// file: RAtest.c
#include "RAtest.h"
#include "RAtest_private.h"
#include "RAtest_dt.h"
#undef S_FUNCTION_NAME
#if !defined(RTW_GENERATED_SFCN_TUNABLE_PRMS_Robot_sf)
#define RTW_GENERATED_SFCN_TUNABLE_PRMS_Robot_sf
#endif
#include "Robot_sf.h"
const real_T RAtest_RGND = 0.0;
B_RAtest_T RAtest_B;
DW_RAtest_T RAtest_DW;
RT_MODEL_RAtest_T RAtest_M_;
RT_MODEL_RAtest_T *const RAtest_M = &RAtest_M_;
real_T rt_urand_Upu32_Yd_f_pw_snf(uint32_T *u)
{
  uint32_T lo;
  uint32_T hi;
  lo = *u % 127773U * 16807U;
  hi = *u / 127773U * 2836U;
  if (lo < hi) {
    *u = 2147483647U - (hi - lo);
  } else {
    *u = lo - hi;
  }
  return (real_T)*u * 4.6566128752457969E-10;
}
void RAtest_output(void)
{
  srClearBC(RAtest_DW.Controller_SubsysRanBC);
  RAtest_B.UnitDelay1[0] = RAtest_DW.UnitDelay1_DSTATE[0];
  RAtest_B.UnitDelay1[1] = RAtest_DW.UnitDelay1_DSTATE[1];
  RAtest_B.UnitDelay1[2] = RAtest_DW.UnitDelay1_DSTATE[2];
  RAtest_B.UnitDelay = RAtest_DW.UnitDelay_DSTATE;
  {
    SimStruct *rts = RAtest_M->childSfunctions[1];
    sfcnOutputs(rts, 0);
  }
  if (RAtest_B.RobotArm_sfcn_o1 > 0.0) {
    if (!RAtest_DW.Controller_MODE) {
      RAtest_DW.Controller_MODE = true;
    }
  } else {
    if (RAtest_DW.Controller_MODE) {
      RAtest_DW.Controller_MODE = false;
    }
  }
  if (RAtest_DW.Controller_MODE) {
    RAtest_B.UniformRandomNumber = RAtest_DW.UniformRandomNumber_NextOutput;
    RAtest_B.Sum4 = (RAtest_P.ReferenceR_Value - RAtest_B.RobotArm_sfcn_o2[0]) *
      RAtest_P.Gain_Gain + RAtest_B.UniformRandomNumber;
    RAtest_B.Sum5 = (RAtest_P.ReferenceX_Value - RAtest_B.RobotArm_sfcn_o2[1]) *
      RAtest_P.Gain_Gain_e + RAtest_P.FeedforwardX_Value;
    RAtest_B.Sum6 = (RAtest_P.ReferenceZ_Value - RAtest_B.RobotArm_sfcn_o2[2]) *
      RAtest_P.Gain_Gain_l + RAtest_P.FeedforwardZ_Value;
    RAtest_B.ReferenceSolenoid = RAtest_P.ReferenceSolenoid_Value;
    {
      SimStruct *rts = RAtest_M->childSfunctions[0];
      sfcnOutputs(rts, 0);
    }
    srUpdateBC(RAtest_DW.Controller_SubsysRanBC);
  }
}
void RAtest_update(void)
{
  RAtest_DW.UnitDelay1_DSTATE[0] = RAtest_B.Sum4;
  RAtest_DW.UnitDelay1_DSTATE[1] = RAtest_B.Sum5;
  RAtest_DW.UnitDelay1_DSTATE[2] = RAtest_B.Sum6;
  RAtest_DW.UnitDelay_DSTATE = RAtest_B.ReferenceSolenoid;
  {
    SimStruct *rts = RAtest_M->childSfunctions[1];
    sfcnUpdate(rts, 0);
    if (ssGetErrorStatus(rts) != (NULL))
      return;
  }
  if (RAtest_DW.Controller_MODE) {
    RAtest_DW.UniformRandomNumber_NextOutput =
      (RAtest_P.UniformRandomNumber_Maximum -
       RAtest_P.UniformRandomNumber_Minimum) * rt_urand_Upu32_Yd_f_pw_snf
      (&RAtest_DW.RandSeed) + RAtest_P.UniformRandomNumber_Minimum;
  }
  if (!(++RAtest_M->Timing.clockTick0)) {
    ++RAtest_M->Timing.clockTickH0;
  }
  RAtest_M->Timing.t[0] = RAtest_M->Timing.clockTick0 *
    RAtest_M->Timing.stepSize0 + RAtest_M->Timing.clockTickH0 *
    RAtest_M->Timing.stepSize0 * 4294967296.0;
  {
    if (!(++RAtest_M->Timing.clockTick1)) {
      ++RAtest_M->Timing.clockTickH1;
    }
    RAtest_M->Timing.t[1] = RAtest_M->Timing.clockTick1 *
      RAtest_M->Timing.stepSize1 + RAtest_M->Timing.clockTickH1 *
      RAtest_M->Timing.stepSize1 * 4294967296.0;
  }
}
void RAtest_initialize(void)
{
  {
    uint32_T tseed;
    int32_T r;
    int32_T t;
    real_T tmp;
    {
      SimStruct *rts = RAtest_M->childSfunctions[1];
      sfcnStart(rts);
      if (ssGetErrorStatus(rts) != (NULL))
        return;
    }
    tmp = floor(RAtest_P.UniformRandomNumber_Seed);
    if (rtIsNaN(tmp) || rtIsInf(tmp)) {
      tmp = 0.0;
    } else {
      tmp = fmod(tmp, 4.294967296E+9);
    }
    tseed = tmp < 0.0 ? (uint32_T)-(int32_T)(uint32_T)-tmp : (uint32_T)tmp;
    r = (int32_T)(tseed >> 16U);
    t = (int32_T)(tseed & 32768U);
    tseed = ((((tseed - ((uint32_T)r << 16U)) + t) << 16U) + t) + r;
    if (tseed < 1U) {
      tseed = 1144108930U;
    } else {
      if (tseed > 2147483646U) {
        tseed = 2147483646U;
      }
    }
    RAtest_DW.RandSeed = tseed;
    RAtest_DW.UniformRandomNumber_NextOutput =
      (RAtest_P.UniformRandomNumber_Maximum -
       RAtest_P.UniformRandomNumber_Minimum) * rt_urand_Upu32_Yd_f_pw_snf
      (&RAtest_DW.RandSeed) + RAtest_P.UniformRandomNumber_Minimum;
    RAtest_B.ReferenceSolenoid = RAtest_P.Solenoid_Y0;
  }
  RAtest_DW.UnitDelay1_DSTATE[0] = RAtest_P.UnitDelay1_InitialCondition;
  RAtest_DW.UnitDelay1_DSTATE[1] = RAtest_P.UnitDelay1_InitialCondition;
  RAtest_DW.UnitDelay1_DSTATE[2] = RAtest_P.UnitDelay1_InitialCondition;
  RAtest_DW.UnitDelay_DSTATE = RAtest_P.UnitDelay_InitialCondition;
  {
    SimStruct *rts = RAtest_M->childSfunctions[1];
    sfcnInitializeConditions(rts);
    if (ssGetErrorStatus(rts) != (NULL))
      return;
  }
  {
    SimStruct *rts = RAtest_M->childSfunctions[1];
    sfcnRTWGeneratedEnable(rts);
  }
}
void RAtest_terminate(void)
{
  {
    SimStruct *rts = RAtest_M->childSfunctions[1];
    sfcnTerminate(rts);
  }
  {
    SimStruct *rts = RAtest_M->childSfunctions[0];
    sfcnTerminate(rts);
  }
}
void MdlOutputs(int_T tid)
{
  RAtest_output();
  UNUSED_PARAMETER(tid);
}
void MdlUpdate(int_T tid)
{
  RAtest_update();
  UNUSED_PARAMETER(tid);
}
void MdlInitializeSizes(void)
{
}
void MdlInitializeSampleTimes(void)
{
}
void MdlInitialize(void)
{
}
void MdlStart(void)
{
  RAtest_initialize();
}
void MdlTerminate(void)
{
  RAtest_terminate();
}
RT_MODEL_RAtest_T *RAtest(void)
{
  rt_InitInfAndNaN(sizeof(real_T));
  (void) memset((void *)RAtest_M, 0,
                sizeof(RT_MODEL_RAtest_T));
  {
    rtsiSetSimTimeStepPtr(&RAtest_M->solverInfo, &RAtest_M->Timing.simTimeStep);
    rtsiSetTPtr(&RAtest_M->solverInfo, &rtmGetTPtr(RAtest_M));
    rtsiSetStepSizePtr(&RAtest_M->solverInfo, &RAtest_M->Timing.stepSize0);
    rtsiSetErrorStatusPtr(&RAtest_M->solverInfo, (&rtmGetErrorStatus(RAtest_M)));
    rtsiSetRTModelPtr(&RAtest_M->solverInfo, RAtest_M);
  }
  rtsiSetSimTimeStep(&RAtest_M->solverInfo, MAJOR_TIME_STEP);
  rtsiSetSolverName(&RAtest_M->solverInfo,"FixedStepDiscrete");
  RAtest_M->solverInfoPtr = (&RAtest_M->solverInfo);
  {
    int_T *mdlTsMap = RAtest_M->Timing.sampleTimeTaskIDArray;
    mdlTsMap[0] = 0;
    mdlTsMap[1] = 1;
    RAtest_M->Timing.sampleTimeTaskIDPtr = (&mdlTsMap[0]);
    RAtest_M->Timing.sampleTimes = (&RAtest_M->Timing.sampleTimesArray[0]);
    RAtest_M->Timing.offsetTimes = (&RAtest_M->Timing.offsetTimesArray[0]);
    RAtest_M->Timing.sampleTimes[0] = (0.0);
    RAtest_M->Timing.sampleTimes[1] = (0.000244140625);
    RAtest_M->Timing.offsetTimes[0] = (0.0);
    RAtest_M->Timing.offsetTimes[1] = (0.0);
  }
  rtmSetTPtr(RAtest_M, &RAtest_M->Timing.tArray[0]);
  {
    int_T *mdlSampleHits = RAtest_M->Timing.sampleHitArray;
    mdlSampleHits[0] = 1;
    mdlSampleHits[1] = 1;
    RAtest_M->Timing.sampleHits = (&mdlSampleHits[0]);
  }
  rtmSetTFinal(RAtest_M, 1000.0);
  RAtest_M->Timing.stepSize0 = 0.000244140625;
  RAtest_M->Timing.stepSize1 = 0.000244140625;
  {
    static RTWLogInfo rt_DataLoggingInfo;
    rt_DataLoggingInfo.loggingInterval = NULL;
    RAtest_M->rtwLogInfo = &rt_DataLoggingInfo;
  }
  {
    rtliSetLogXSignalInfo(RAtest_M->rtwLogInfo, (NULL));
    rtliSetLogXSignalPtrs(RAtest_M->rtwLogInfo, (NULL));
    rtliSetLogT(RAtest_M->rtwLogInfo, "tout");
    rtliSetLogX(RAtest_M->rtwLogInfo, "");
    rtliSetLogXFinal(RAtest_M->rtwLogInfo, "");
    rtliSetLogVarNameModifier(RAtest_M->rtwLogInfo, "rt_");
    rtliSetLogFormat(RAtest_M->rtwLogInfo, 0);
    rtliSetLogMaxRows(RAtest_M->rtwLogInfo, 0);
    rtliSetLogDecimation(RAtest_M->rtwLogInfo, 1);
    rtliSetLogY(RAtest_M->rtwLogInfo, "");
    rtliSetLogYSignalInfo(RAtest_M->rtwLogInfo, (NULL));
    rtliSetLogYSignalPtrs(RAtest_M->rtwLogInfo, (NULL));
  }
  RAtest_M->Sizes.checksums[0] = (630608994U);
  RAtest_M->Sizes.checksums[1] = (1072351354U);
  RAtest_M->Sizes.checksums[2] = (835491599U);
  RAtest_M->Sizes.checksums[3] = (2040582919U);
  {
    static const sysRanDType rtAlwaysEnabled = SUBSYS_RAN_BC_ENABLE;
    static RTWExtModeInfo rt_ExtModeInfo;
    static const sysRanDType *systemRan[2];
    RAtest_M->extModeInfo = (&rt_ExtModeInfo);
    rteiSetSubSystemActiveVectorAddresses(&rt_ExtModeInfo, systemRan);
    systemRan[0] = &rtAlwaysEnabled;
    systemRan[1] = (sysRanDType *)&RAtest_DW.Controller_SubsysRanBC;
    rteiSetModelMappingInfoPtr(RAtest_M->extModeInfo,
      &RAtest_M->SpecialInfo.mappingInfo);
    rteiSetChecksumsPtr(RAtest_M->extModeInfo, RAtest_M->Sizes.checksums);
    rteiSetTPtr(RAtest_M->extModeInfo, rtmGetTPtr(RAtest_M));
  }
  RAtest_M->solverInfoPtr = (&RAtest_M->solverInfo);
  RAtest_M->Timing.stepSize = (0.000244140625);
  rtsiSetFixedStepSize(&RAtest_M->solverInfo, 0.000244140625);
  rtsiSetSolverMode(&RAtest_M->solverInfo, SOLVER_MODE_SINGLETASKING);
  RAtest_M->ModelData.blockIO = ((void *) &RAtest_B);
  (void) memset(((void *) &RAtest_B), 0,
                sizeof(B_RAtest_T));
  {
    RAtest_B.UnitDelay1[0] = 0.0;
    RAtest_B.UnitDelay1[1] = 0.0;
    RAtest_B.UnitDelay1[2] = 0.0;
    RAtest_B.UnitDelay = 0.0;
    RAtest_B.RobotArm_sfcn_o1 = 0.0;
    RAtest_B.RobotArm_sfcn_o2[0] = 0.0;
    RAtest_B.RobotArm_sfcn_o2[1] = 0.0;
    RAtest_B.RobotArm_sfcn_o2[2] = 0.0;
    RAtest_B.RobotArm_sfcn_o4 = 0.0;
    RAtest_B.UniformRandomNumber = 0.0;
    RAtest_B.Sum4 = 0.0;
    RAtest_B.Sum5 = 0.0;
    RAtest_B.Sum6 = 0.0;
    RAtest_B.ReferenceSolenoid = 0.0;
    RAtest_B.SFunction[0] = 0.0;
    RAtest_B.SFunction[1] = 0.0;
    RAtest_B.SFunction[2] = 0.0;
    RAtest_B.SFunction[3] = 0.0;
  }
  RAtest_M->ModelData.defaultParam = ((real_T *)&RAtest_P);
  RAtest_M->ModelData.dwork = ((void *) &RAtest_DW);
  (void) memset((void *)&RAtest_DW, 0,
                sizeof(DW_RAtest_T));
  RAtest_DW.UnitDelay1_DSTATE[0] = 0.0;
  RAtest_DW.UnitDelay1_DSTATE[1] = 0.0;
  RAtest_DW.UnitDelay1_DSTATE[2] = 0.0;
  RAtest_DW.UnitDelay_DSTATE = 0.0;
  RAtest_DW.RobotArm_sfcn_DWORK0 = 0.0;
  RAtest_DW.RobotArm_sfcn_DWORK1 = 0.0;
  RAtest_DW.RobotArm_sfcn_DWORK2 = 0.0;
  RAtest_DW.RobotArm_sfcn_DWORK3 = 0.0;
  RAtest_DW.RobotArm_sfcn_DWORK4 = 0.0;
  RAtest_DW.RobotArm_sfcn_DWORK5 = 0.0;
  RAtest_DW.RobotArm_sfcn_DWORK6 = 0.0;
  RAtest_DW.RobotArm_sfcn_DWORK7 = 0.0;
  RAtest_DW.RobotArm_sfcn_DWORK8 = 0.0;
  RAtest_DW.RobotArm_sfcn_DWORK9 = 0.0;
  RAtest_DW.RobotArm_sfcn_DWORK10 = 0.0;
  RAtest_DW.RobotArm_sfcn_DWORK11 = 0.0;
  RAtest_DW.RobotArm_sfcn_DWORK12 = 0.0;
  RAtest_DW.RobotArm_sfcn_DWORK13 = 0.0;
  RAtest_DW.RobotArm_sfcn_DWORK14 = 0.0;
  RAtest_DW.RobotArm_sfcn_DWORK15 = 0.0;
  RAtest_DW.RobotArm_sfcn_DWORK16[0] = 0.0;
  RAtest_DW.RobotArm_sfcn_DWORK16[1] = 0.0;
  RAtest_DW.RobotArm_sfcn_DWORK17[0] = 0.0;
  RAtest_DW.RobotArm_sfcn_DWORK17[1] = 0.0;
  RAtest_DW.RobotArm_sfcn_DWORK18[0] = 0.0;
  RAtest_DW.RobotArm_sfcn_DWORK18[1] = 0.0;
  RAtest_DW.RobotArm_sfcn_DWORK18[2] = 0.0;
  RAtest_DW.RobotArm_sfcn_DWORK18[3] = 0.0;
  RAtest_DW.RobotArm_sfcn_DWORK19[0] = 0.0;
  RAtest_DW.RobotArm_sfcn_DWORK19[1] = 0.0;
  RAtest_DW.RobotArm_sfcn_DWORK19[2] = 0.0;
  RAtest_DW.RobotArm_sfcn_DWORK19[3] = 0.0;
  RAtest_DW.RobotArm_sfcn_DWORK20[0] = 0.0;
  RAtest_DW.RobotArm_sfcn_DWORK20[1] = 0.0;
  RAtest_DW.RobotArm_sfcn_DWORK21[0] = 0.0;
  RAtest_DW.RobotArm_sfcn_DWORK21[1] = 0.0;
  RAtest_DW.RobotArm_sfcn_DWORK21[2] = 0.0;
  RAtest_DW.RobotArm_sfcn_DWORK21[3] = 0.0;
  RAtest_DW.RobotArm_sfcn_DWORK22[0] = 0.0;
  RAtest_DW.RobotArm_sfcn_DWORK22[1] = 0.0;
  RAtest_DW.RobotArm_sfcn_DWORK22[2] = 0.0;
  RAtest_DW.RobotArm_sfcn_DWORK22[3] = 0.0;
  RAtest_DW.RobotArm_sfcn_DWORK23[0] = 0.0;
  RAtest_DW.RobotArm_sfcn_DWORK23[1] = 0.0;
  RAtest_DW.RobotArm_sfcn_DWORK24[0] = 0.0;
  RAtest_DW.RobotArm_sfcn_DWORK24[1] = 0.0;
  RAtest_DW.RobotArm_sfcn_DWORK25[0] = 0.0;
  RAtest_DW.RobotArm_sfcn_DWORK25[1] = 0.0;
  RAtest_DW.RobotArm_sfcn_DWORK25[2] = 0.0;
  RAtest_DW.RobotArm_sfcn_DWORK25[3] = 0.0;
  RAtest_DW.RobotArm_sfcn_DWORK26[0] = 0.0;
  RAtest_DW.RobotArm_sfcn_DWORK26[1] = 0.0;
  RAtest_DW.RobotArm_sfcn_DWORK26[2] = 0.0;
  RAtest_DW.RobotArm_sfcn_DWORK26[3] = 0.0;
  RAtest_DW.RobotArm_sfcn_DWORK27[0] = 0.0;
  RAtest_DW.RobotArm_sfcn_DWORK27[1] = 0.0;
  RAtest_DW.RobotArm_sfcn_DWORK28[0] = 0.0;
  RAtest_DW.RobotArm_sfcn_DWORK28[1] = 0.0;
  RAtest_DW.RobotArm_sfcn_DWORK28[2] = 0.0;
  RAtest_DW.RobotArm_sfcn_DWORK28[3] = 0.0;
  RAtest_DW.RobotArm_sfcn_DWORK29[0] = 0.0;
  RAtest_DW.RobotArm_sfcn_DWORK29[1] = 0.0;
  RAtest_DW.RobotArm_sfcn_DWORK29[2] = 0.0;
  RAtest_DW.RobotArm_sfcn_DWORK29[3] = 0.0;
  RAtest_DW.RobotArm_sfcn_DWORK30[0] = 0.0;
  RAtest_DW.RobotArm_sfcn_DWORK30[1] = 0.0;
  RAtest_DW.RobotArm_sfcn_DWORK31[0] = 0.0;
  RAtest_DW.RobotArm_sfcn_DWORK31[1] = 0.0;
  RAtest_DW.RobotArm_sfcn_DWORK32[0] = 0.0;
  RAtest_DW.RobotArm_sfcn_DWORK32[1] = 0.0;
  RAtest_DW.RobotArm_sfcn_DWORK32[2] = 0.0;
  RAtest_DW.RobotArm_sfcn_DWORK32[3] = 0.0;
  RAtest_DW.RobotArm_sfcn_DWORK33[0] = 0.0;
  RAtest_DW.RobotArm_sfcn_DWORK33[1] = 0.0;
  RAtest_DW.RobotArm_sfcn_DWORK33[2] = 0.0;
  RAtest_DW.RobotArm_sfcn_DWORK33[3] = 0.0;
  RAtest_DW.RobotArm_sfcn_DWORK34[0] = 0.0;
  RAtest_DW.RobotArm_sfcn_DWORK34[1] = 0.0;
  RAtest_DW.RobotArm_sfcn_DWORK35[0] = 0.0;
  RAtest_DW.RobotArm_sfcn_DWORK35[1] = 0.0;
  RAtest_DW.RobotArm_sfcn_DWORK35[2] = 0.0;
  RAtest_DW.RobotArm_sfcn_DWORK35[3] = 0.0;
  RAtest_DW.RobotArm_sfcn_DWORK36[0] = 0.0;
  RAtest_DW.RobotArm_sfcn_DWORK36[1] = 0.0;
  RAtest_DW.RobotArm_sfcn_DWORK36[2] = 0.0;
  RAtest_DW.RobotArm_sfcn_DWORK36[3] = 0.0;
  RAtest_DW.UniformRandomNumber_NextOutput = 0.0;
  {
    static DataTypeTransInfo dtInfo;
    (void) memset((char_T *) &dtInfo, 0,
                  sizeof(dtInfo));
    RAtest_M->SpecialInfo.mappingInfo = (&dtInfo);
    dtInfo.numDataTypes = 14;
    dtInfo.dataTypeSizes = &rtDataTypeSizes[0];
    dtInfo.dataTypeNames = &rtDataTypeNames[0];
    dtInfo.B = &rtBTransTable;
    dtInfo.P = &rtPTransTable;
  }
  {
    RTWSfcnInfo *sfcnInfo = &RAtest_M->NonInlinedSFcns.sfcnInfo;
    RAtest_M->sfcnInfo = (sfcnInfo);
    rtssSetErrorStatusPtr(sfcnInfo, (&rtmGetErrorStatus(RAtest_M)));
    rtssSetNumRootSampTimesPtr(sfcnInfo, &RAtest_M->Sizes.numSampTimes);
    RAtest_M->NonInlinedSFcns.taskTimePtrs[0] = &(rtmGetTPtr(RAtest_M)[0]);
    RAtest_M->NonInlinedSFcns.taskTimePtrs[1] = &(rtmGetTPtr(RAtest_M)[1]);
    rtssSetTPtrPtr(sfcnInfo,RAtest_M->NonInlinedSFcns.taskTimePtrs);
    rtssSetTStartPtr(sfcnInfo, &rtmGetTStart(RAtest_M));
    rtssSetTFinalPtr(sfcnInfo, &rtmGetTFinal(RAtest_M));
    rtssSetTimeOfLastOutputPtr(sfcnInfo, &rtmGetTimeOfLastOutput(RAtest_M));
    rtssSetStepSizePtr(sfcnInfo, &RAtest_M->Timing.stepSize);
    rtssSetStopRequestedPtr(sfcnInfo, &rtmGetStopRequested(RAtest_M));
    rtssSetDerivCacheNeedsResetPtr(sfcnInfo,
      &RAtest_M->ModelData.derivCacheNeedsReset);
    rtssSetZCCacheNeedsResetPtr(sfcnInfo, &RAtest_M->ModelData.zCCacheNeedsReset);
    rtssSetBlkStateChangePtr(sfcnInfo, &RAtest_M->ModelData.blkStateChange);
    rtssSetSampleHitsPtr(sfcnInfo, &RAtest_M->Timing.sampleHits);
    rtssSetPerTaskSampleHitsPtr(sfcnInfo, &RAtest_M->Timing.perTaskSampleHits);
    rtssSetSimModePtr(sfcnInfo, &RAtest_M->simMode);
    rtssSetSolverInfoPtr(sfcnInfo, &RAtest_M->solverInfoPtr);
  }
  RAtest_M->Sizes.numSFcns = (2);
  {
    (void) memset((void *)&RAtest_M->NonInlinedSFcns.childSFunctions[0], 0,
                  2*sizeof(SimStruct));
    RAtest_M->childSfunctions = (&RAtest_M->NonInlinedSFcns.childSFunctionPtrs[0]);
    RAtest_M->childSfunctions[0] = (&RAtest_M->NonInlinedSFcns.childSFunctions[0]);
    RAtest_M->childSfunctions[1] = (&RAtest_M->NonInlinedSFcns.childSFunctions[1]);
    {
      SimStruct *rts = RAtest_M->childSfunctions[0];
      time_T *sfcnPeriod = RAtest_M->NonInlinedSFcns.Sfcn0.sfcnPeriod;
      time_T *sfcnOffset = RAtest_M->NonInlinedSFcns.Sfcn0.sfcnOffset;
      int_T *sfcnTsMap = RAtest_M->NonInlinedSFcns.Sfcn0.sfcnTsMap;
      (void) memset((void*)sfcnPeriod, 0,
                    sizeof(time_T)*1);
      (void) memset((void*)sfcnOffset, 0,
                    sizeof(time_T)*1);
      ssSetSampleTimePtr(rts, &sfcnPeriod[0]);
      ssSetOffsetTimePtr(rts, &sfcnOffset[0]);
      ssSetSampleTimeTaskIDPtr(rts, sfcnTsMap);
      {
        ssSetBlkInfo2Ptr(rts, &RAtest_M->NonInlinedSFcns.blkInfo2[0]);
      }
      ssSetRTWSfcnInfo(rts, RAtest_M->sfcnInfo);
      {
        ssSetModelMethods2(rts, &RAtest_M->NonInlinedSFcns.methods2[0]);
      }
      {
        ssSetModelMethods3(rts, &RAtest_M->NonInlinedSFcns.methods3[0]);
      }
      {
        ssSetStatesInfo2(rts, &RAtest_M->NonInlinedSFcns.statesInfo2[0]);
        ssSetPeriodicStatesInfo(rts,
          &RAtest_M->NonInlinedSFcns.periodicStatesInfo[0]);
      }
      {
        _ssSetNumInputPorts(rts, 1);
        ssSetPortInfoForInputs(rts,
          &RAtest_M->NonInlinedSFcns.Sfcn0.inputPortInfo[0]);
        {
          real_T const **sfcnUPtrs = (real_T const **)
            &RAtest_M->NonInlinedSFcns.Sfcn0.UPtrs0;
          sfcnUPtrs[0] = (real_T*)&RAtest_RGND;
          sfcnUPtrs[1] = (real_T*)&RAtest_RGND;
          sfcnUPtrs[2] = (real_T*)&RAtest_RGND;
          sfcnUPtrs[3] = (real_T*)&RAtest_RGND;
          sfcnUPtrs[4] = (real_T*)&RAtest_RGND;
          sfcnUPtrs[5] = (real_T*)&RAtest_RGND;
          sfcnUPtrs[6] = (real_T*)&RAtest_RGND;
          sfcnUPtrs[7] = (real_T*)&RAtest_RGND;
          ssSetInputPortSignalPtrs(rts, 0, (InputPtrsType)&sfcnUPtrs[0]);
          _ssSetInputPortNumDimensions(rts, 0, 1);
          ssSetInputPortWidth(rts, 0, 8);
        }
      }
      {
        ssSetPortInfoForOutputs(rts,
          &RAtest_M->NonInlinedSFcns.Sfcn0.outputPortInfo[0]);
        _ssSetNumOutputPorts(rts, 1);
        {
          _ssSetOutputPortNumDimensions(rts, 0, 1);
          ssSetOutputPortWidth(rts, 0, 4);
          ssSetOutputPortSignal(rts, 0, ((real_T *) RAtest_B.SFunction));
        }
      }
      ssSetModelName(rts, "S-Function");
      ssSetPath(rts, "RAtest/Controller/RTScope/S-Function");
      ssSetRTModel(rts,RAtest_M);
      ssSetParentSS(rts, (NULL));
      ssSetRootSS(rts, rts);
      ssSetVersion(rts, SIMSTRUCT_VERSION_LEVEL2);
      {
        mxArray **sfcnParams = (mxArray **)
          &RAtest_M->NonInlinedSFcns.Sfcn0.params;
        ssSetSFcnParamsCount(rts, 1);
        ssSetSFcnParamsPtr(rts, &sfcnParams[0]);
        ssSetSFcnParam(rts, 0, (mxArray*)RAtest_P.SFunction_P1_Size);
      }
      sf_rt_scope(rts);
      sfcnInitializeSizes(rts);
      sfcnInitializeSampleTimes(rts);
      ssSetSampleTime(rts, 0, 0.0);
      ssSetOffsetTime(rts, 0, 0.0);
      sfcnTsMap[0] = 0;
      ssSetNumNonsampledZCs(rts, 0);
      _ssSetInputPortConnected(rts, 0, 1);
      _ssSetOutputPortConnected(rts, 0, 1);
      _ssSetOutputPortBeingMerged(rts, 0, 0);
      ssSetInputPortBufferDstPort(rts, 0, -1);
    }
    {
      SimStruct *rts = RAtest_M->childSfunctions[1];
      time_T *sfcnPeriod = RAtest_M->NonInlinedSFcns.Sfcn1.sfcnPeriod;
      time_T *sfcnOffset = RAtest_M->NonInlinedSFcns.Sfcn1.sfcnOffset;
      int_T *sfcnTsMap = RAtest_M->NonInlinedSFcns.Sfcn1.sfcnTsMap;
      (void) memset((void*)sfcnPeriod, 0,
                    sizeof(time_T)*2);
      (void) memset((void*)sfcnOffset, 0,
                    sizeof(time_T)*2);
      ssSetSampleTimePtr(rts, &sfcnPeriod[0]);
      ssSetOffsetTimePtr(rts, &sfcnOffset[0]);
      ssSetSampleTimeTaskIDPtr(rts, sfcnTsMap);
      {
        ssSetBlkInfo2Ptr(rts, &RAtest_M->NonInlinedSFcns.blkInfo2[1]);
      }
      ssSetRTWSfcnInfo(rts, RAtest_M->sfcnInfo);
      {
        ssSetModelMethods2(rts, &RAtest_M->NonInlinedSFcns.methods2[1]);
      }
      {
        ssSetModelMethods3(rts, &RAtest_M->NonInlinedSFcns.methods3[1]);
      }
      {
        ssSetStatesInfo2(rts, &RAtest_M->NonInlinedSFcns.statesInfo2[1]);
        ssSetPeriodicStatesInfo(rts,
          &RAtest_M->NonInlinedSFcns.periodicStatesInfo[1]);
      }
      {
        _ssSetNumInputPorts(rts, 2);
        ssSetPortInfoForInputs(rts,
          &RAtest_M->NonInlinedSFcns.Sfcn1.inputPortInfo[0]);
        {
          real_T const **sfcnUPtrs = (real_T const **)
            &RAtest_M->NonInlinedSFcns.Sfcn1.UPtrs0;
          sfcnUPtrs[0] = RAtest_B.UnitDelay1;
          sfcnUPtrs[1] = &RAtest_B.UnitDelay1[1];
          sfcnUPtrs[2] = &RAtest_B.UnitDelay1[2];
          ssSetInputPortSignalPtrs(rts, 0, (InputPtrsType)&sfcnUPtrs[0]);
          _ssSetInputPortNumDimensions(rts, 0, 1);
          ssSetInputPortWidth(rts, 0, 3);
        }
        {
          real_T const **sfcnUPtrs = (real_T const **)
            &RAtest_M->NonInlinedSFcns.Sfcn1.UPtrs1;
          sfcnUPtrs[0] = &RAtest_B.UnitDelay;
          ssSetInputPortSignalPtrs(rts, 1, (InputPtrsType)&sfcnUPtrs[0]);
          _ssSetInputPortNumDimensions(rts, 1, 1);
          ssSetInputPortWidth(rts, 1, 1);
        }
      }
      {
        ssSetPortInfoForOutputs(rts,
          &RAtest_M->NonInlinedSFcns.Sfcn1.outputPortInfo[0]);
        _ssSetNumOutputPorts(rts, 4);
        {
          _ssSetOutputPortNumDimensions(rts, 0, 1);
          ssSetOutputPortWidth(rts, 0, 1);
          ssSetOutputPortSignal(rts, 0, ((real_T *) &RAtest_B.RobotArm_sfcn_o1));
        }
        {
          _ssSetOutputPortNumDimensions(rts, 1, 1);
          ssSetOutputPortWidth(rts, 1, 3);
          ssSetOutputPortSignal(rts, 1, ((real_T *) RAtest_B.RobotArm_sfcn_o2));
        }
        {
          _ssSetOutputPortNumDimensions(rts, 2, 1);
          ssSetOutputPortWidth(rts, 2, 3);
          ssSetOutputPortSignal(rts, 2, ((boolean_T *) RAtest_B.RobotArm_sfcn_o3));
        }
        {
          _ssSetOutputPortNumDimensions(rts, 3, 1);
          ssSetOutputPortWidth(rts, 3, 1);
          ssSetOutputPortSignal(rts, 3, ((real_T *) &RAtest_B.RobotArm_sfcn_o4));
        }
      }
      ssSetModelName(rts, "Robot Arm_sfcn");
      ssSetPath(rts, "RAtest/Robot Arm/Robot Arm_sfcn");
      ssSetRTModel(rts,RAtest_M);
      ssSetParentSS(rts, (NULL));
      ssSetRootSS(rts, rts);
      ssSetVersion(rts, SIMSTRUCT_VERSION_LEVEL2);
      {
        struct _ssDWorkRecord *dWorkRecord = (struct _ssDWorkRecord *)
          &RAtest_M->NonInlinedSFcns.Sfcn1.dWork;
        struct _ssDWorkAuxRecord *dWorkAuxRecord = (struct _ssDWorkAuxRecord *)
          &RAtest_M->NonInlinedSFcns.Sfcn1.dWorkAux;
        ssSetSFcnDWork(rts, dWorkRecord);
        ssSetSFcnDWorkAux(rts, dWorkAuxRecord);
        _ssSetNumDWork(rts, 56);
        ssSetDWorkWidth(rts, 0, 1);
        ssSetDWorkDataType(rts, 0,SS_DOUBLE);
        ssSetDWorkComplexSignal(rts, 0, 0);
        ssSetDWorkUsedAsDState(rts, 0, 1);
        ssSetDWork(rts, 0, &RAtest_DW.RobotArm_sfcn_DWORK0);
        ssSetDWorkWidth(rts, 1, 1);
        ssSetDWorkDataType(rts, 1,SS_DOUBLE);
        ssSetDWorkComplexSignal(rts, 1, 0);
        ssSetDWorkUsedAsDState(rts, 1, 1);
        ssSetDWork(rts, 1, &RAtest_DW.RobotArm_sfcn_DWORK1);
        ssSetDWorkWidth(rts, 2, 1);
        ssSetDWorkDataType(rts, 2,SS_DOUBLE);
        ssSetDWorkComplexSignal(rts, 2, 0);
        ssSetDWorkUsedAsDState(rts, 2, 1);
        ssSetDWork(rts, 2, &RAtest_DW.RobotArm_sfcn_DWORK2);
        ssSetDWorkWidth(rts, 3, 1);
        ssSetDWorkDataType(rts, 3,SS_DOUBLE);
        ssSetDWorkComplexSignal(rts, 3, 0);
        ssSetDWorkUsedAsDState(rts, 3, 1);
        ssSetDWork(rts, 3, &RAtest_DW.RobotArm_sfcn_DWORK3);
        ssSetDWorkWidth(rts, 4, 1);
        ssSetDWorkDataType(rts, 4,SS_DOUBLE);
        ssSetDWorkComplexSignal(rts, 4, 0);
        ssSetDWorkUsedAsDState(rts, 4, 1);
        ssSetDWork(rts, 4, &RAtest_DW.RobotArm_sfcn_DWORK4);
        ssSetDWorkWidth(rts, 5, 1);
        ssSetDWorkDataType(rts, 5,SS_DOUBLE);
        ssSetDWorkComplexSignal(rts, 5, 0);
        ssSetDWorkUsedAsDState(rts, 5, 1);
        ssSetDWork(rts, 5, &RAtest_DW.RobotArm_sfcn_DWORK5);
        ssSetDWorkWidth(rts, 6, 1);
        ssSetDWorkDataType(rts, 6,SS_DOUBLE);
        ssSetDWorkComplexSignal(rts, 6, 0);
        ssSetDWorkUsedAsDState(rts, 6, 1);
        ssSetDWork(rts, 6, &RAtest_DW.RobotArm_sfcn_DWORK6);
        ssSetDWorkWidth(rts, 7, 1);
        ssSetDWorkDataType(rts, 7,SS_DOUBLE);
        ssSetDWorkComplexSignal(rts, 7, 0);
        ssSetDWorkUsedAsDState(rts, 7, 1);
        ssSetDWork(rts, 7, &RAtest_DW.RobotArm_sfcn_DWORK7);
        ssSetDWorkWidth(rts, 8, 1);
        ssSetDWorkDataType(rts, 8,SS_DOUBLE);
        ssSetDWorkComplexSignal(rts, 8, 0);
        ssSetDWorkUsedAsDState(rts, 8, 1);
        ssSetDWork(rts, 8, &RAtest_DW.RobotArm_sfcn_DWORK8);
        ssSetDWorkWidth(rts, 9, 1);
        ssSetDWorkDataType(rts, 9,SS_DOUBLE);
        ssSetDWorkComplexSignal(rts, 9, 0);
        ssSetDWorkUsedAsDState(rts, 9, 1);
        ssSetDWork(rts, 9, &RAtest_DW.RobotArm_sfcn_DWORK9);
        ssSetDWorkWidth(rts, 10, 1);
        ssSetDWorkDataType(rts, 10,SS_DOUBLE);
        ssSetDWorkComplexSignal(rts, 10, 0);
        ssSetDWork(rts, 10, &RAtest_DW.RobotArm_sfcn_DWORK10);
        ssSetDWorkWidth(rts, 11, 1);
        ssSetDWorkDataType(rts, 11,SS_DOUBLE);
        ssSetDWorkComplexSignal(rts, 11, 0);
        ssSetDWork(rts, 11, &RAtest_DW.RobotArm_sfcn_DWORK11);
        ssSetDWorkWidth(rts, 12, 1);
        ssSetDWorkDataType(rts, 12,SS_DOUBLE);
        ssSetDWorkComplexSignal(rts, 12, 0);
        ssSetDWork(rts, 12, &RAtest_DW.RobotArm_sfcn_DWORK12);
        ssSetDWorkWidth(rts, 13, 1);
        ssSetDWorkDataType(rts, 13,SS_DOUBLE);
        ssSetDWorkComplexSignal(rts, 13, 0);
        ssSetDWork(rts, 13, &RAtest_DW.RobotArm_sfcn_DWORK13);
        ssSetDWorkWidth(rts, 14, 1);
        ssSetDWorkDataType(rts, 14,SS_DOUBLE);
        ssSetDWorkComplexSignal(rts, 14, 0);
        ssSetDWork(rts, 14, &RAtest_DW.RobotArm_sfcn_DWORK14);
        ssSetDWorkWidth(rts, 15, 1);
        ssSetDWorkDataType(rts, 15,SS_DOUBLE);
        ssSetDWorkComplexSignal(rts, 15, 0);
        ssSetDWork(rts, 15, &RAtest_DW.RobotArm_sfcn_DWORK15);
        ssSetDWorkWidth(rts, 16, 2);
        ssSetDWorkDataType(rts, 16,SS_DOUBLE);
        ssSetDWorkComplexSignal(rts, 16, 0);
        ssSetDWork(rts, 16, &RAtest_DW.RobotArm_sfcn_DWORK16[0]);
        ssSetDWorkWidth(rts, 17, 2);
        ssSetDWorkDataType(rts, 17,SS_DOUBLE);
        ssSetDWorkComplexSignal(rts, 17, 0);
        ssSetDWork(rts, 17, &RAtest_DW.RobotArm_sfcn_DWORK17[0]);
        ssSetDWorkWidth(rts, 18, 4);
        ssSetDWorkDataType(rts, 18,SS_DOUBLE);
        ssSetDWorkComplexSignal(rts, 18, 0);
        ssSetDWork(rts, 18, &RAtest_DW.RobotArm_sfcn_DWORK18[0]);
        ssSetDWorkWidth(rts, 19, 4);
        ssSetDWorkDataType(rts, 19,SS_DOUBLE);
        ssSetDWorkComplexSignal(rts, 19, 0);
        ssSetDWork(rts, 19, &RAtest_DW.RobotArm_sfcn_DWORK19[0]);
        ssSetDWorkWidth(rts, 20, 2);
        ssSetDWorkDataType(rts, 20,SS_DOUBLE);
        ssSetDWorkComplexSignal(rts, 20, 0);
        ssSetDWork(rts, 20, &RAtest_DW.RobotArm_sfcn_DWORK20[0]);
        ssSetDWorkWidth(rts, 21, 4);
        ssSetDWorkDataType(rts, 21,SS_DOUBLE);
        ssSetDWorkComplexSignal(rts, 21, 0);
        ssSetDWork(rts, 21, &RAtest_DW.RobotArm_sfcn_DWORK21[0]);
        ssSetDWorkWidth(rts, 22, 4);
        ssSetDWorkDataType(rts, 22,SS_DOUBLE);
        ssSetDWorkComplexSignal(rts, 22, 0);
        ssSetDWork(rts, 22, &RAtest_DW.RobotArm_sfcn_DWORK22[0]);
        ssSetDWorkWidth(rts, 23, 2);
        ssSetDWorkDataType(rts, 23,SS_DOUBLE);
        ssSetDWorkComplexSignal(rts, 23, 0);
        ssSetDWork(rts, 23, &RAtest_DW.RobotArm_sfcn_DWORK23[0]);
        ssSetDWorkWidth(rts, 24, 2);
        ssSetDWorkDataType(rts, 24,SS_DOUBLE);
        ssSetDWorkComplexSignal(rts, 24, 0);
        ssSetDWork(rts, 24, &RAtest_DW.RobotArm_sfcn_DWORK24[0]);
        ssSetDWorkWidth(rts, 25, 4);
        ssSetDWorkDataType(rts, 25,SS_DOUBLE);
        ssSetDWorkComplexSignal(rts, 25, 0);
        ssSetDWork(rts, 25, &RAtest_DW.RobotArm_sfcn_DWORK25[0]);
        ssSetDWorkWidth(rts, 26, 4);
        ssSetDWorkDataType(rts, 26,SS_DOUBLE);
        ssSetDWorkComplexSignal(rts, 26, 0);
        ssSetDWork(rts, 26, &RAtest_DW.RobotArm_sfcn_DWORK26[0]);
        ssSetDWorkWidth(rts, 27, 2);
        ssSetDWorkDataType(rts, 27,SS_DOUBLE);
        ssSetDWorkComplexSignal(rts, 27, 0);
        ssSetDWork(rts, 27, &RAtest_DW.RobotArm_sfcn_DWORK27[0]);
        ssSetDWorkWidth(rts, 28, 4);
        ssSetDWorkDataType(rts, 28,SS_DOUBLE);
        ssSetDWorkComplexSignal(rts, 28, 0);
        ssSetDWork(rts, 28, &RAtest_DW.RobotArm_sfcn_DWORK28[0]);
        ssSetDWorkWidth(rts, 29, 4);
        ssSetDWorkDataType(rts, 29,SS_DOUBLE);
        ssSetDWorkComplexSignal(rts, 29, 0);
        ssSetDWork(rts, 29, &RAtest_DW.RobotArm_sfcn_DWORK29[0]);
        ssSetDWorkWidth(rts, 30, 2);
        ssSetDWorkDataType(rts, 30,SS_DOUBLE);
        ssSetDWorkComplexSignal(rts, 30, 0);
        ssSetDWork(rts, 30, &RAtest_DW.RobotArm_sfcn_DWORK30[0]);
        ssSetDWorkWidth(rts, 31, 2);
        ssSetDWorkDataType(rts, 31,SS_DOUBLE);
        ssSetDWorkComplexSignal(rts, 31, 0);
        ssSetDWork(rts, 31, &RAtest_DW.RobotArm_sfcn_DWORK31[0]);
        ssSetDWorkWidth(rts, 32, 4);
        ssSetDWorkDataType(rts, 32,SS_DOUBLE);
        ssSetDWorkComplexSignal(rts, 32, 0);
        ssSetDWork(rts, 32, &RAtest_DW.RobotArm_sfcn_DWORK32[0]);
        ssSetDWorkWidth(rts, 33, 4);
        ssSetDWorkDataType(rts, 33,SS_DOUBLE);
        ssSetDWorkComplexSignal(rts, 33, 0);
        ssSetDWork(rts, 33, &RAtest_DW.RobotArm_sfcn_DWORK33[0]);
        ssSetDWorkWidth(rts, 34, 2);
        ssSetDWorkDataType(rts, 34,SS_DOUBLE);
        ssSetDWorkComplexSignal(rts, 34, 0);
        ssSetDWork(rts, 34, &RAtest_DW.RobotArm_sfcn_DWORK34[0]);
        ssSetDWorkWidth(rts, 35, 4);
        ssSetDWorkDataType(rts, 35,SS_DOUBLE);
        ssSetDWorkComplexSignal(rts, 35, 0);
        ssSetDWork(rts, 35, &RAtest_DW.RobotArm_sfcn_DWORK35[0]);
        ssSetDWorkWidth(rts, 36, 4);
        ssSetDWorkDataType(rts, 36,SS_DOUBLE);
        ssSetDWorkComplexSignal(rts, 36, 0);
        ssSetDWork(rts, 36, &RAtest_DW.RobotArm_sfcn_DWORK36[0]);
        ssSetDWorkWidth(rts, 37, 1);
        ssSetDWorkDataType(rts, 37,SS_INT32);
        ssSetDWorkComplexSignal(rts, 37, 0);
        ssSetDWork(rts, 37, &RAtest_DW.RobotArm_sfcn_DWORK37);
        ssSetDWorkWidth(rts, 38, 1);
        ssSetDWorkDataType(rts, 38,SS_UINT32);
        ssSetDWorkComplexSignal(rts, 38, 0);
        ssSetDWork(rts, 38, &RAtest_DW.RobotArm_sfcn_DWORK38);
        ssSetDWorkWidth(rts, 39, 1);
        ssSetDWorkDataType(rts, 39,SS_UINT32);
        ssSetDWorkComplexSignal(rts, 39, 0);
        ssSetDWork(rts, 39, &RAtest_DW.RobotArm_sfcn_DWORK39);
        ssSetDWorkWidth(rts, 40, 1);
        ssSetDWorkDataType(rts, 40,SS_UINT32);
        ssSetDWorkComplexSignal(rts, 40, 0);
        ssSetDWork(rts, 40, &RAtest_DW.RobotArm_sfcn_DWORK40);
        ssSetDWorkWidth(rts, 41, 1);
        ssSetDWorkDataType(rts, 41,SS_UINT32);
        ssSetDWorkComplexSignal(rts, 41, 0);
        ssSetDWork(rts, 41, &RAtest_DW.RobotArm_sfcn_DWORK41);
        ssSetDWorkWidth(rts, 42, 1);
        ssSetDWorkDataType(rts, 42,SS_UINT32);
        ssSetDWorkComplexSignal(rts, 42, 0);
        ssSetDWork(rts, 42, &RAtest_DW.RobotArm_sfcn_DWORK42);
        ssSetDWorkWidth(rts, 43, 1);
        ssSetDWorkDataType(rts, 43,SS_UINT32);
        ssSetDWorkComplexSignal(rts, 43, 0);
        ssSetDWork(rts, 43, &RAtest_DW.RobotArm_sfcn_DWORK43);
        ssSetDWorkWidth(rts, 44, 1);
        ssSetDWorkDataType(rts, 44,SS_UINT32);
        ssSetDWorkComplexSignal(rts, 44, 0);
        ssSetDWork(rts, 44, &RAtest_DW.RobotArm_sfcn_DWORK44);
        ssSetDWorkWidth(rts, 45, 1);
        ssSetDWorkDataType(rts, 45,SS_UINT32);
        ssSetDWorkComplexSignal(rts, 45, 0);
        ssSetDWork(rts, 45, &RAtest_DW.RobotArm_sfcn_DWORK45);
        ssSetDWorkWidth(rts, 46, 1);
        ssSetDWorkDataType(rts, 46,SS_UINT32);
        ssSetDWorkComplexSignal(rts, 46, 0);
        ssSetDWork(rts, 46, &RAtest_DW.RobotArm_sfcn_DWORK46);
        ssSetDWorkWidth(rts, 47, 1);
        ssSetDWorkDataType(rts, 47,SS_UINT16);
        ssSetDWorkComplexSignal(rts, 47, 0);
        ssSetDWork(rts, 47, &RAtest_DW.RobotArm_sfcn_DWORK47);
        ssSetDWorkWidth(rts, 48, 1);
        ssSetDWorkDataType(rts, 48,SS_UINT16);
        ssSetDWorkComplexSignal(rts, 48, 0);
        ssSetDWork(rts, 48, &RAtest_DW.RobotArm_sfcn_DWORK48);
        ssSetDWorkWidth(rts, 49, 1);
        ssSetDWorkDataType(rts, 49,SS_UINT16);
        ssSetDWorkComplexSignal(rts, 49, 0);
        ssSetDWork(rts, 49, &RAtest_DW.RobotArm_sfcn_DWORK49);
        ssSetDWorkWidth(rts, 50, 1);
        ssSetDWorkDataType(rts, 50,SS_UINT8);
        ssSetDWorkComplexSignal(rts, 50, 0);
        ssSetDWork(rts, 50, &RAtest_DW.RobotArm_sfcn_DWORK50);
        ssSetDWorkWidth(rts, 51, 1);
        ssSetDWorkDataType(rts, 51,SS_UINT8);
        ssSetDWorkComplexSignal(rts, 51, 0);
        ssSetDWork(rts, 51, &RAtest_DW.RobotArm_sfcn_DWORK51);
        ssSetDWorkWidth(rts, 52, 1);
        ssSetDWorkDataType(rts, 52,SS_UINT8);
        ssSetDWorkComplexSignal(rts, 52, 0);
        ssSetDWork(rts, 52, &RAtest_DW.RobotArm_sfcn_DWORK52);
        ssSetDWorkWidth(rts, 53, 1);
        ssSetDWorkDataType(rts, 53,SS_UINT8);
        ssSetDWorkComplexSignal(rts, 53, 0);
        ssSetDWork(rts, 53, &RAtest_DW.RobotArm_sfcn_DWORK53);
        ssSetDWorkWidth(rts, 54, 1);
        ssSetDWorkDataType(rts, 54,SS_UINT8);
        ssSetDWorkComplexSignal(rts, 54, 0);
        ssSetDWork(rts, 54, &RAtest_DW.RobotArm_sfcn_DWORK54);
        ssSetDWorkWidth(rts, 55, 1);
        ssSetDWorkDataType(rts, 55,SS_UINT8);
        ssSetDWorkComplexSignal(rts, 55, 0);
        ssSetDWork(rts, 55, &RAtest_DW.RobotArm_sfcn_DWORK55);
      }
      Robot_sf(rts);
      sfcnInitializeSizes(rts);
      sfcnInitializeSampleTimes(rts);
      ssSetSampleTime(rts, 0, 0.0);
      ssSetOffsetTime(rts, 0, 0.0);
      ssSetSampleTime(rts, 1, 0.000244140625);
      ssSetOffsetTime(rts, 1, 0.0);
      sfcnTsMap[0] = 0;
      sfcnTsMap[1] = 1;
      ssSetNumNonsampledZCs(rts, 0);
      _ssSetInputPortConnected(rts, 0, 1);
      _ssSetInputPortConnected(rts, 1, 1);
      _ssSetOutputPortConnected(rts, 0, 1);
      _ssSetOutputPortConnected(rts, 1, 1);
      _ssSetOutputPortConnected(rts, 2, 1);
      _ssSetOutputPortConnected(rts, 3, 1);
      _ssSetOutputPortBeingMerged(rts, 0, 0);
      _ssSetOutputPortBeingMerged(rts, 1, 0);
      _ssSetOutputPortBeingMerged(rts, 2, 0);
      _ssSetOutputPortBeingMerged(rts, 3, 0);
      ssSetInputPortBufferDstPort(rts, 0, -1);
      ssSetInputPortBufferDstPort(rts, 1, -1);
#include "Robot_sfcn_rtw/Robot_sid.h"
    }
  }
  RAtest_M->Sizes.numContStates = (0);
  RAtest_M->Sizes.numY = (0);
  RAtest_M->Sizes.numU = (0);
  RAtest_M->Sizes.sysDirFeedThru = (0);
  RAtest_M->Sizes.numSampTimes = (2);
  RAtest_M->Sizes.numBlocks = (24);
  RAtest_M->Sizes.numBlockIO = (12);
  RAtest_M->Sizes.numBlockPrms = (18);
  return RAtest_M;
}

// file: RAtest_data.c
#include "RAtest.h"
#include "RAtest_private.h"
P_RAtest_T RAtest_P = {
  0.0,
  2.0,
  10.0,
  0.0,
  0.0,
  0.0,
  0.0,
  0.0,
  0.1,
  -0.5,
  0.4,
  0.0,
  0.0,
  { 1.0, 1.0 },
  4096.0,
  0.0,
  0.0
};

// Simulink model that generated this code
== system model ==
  UnitDelay1 : UnitDelay  <- 1: Controller
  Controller : Subsystem  <- 1: RobotArm_sfcn/2, Enable: RobotArm_sfcn
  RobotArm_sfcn : S-Function  FunctionName=Robot_sf  <- 1: UnitDelay1, 2: UnitDelay
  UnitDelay : UnitDelay  <- 1: Controller/2
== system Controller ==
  Inport#1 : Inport
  EnablePort#1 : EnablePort
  Outport#1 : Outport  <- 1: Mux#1
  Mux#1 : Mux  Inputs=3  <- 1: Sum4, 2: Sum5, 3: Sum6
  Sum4 : Sum  Inputs=++  <- 1: UniformRandomNumber, 2: Gain
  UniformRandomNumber : UniformRandomNumber
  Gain : Gain  Gain=10  <- 1: Sum#1
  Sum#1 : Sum  Inputs=+-  <- 1: ReferenceR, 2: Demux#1
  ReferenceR : Constant  Value=2
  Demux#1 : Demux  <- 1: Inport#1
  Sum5 : Sum  Inputs=++  <- 1: FeedforwardX, 2: Gain#1
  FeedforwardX : Constant  Value=0
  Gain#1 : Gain  Gain=0  <- 1: Sum#2
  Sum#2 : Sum  Inputs=+-  <- 1: ReferenceX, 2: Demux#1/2
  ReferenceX : Constant  Value=0
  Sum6 : Sum  Inputs=++  <- 1: FeedforwardZ, 2: Gain#2
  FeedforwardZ : Constant  Value=0.1
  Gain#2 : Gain  Gain=0  <- 1: Sum#3
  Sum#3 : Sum  Inputs=+-  <- 1: ReferenceZ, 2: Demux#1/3
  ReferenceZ : Constant  Value=0
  Solenoid : Outport  InitialOutput=0  <- 1: ReferenceSolenoid
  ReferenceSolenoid : Constant  Value=0
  SFunction : S-Function  FunctionName=sf_rt_scope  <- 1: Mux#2
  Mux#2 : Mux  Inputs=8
